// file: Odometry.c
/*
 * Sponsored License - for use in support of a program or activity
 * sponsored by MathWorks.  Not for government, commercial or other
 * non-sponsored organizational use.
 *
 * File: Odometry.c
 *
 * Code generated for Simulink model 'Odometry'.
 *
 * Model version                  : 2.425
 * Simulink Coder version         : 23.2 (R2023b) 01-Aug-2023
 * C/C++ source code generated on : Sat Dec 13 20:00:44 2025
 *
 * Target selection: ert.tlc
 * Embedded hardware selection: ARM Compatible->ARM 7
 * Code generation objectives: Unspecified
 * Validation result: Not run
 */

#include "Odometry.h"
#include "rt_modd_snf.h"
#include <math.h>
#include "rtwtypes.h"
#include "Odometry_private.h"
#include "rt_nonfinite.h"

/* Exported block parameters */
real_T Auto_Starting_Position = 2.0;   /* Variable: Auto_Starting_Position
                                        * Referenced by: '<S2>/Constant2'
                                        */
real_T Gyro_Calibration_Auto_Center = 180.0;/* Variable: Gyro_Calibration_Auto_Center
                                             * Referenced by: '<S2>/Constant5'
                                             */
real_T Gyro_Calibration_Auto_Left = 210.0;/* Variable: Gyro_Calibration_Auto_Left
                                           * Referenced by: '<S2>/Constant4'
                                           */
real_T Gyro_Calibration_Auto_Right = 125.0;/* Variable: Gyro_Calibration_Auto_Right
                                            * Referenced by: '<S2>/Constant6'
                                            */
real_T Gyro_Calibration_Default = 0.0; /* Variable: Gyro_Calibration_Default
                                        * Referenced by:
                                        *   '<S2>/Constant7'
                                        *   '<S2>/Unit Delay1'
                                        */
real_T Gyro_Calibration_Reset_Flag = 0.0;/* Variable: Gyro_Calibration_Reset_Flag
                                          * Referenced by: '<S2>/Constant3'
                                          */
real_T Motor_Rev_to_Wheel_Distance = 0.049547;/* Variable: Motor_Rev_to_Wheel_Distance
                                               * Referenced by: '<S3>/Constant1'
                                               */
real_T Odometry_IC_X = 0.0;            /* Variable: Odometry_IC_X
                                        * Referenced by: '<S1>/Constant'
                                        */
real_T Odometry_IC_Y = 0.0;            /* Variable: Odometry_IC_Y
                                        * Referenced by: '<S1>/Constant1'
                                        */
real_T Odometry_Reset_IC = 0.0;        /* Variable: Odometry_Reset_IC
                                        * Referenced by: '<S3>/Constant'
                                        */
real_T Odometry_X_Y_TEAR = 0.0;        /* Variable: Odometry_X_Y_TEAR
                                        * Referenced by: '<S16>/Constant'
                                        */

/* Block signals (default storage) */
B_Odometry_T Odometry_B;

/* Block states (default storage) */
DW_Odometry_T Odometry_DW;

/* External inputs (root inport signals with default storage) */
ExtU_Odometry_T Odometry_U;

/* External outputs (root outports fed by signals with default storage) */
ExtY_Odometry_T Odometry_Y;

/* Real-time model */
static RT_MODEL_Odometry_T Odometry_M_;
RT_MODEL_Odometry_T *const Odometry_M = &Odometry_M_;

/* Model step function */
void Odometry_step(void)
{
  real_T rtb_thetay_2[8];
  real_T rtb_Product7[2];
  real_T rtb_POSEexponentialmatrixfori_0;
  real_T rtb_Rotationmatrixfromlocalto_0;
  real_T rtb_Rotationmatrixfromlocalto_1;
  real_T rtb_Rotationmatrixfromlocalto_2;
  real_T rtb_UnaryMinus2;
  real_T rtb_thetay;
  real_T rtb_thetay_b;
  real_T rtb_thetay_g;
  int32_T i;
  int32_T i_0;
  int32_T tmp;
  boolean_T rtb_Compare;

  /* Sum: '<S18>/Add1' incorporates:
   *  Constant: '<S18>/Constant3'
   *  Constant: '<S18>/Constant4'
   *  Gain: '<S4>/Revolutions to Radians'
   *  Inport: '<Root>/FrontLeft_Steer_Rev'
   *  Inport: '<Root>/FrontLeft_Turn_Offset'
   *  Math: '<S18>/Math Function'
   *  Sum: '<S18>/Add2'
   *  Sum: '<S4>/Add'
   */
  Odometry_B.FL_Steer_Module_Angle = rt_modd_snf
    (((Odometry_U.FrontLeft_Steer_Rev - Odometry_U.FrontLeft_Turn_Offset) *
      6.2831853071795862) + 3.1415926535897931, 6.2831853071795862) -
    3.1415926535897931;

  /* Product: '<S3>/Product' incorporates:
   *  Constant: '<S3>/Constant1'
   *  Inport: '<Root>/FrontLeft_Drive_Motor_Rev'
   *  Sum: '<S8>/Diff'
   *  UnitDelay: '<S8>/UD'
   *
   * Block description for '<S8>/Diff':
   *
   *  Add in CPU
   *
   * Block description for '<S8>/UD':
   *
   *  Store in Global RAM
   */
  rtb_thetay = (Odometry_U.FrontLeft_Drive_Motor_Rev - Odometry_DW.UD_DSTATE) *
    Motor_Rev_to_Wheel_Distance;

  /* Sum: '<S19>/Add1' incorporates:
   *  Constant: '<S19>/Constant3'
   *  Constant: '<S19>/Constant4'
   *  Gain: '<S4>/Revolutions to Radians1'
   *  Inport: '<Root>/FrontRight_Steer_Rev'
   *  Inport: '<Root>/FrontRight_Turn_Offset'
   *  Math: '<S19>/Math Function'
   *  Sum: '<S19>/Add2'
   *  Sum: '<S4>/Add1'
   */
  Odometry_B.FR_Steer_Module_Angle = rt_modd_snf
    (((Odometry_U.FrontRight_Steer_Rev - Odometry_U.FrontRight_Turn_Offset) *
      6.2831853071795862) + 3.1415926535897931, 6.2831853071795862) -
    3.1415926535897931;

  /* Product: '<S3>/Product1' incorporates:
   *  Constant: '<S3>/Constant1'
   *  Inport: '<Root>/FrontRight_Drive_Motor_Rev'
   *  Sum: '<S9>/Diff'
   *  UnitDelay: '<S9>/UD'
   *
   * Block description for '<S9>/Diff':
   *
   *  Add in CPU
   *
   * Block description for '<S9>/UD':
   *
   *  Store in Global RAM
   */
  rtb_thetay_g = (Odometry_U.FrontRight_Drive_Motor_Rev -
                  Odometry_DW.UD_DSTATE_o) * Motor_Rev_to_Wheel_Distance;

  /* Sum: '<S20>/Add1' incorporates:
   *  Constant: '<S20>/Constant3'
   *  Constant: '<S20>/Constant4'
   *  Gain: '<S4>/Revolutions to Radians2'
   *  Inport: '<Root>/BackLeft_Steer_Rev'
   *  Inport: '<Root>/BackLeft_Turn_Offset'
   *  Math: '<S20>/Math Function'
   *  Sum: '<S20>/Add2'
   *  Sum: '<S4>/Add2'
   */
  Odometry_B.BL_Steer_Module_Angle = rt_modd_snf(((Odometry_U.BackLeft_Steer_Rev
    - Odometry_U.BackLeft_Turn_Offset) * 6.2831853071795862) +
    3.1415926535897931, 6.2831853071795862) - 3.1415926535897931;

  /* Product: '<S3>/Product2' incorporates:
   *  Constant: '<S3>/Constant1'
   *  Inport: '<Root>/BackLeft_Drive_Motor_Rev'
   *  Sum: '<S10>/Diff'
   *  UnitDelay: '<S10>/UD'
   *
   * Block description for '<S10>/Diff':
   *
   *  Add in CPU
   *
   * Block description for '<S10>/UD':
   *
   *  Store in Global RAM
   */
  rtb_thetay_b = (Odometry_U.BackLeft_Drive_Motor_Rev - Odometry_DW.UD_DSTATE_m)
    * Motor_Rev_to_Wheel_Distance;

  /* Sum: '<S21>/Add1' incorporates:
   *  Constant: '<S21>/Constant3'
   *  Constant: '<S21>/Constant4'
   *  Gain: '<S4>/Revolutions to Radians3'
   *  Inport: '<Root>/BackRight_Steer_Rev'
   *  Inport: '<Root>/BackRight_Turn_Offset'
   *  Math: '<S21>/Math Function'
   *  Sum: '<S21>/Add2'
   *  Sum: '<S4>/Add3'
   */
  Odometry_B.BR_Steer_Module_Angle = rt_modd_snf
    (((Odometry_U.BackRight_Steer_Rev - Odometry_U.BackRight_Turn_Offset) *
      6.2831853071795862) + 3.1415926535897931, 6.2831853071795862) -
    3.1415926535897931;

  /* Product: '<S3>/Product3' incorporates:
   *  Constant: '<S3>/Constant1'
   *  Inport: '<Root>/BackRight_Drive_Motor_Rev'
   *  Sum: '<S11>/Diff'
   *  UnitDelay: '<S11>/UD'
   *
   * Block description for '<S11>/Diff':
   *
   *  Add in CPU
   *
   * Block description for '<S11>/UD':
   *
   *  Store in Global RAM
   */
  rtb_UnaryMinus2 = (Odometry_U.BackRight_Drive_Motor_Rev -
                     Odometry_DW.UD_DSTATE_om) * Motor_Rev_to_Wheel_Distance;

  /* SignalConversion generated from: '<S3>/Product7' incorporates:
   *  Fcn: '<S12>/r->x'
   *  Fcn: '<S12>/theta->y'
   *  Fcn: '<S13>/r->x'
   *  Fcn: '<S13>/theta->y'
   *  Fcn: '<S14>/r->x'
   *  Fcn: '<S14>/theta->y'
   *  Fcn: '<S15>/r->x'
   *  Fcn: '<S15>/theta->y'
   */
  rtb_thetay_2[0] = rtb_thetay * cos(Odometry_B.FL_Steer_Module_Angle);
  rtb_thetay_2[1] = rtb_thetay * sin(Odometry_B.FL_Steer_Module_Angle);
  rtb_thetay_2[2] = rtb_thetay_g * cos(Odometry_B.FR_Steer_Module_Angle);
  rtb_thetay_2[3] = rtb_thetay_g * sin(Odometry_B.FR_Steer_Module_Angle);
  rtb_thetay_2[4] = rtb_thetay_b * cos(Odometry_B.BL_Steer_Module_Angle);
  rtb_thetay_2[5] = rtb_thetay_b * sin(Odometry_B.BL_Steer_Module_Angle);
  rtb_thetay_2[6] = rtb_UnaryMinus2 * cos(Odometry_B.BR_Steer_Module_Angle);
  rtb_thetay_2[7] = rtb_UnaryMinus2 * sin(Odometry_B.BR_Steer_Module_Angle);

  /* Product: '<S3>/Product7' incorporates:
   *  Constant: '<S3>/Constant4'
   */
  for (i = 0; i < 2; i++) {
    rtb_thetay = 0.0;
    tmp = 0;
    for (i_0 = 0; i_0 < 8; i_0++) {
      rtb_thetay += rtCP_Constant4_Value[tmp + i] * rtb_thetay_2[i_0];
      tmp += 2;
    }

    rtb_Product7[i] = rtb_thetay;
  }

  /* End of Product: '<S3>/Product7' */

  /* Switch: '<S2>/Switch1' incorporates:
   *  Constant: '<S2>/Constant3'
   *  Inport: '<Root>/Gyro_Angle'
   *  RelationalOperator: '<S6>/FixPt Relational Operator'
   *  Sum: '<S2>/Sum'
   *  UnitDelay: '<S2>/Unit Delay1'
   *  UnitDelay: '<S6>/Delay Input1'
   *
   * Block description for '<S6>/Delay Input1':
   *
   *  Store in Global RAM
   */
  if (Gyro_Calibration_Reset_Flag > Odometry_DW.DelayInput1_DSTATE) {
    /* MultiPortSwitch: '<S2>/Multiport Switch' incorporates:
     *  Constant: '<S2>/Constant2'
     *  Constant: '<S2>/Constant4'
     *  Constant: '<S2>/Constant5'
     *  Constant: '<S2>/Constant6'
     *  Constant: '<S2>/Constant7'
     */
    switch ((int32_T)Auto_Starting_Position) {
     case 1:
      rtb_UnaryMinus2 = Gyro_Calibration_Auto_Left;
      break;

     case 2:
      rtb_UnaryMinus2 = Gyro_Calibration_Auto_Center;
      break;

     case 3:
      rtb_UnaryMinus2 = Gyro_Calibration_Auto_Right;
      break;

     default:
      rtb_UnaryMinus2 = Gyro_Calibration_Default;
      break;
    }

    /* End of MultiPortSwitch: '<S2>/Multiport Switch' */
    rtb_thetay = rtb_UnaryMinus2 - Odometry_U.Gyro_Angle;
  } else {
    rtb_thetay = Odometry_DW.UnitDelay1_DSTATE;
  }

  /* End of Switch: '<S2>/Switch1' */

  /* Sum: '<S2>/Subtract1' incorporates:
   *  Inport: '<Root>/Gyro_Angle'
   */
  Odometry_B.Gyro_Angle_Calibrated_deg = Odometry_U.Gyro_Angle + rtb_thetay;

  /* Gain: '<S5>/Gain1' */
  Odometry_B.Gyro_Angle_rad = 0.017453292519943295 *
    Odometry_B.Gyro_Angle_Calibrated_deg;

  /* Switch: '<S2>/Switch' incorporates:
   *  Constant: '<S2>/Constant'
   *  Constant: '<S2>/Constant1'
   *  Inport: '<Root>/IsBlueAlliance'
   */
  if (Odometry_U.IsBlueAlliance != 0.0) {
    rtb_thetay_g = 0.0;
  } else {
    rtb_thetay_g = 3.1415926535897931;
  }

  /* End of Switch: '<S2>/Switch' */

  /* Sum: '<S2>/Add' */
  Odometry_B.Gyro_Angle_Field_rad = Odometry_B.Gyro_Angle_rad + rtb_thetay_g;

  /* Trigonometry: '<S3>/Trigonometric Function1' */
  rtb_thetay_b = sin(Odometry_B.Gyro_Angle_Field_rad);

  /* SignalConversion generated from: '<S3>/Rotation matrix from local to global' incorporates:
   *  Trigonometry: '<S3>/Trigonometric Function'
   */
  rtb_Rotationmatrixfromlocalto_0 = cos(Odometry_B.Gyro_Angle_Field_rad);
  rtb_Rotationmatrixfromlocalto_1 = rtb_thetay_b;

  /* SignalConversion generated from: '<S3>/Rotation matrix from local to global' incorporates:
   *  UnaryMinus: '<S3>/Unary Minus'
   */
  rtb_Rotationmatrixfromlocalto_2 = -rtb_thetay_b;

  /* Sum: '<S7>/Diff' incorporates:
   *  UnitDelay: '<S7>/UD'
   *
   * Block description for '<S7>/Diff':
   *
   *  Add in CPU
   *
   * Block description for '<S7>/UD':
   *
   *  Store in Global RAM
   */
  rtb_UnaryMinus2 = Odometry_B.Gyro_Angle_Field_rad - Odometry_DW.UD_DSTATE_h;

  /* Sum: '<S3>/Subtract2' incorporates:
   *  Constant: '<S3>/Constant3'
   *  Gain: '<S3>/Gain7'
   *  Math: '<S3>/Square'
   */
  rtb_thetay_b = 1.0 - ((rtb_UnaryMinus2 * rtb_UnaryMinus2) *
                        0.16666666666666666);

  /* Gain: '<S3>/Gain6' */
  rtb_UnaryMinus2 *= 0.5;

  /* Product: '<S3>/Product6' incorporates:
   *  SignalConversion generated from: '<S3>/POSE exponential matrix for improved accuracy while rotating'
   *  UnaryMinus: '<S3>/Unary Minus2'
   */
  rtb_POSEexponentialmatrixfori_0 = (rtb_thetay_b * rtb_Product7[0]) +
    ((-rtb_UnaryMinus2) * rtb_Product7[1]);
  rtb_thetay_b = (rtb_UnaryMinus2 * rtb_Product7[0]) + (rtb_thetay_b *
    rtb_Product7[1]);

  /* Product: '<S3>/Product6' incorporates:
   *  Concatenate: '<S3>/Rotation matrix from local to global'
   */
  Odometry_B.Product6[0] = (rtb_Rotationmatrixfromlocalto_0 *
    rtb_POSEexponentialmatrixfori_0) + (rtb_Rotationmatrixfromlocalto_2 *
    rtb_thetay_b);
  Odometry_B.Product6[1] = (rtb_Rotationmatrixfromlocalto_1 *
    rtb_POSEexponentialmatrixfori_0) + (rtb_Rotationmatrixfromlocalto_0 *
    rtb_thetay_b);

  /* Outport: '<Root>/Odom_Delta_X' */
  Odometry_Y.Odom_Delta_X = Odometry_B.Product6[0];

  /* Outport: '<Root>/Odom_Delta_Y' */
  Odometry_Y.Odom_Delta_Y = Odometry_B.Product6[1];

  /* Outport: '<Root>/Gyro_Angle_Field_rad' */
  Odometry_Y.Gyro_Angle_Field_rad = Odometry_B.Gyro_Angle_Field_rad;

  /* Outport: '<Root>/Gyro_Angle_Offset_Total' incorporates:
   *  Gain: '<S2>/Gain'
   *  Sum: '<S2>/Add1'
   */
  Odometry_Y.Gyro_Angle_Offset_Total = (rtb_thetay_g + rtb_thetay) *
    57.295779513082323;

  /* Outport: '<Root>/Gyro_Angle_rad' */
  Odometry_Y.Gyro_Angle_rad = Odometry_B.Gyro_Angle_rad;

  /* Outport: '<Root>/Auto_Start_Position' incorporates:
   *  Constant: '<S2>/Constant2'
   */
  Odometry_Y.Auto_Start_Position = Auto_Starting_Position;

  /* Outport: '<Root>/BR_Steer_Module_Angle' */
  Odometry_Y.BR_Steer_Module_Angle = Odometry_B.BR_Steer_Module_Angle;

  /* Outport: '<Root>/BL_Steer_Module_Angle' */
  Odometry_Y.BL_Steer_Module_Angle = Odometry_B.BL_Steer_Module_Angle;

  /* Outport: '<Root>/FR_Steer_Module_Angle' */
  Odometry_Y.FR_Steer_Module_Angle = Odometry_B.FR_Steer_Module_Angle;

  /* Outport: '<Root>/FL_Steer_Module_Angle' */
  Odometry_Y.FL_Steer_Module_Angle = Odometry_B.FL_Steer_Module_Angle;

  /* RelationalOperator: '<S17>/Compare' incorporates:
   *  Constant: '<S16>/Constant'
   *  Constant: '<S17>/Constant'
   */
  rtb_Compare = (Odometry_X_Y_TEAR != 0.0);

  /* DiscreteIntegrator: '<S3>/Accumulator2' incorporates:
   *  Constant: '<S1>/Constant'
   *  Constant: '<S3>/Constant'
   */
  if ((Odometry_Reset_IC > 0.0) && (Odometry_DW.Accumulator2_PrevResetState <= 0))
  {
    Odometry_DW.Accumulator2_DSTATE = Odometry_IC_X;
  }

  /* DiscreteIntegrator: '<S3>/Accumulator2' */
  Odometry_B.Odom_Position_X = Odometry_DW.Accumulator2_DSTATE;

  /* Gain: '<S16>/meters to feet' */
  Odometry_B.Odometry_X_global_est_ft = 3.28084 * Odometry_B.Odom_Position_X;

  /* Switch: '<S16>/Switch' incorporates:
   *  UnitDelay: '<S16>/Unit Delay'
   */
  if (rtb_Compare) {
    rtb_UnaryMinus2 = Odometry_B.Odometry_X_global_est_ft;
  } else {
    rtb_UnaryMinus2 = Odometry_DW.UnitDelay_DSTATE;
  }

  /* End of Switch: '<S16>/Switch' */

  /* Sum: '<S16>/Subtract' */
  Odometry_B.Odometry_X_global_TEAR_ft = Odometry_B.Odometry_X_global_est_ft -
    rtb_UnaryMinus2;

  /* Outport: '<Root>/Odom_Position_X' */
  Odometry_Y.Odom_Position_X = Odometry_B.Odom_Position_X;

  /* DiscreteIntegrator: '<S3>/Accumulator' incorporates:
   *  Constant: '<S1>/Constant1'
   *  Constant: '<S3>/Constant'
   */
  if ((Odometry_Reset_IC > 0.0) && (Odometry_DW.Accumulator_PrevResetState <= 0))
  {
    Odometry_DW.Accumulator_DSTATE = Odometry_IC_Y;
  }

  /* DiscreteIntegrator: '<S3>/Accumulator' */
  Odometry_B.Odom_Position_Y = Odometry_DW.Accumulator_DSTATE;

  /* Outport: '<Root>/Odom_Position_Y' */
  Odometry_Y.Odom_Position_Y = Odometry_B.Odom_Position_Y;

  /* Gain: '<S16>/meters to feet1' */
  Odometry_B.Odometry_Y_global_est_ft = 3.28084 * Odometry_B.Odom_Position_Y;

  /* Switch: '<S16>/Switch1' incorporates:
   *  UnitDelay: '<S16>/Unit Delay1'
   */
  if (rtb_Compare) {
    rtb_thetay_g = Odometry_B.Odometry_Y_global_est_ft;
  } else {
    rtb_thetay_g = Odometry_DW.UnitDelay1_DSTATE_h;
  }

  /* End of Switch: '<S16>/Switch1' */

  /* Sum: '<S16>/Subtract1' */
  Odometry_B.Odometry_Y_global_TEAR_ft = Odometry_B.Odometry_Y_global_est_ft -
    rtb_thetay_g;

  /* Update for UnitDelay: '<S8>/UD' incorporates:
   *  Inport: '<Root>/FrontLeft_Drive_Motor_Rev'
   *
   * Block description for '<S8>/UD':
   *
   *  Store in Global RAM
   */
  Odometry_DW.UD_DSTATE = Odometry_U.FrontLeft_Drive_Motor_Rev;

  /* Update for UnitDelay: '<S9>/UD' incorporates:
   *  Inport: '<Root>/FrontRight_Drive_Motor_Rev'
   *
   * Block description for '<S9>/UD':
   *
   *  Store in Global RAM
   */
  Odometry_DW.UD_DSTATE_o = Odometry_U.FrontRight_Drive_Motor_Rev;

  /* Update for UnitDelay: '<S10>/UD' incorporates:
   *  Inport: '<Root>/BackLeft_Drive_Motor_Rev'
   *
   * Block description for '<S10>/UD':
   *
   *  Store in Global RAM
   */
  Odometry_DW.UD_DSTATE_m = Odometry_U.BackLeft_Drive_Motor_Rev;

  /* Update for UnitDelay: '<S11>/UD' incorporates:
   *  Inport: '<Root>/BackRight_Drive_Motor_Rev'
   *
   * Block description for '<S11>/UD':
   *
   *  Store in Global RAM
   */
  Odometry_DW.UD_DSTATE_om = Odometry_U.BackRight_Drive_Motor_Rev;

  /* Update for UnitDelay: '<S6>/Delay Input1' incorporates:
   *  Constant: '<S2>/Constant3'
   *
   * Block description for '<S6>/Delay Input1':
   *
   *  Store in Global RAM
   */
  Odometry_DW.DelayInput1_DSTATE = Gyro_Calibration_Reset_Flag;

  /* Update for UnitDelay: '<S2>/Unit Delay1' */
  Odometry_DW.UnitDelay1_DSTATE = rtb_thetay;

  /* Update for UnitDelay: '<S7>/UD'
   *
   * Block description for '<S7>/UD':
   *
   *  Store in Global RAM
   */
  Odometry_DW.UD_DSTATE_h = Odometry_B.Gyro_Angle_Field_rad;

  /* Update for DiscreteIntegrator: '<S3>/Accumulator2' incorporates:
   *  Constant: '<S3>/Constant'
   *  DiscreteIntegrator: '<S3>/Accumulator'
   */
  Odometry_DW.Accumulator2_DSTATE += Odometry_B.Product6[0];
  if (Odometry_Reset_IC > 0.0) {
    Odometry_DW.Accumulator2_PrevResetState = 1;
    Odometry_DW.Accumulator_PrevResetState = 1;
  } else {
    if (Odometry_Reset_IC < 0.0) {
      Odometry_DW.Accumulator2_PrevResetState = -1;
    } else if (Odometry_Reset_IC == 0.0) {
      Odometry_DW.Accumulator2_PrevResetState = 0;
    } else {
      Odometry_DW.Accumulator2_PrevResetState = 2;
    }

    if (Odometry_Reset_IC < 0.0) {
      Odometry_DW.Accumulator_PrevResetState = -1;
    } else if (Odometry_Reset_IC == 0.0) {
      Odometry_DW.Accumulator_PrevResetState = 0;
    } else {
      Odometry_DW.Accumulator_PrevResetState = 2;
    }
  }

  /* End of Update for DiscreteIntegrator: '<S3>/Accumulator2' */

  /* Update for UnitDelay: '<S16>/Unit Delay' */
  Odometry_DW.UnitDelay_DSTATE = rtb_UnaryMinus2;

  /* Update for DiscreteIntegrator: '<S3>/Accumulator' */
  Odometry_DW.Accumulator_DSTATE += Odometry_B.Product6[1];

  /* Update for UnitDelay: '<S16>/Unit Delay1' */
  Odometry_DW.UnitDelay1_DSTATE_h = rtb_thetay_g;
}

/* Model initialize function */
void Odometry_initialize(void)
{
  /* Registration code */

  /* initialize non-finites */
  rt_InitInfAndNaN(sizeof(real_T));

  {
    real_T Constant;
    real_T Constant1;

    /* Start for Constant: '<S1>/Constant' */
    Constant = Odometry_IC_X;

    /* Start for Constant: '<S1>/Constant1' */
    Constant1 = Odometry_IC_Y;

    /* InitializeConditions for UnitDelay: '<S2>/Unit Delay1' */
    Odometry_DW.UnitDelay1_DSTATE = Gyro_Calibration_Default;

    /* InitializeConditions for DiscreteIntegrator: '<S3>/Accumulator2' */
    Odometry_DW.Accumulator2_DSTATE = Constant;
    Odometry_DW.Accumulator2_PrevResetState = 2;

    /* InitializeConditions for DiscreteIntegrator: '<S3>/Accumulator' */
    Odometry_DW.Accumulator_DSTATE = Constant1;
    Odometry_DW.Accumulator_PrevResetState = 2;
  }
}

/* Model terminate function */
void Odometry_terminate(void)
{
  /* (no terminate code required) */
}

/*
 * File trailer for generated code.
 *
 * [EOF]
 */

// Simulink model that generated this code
simulink model "Odometry"  (R2023b)
settings: Solver=FixedStepDiscrete  StartTime=0.0  StopTime=inf  FixedStep=t_sample_fast  RelTol=1e-3
undefined symbols (not defined in the file): Odometry_IC_X, Odometry_IC_Y, t_sample_fast

== system Odometry ==
  IsBlueAlliance : Inport
  Gyro_Angle : Inport  Port=2
  FrontLeft_Drive_Motor_Rev : Inport  Port=3
  FrontRight_Drive_Motor_Rev : Inport  Port=4
  BackLeft_Drive_Motor_Rev : Inport  Port=5
  BackRight_Drive_Motor_Rev : Inport  Port=6
  FrontLeft_Steer_Rev : Inport  Port=7
  FrontRight_Steer_Rev : Inport  Port=8
  BackLeft_Steer_Rev : Inport  Port=9
  BackRight_Steer_Rev : Inport  Port=10
  FrontLeft_Turn_Offset : Inport  Port=11
  FrontRight_Turn_Offset : Inport  Port=12
  BackLeft_Turn_Offset : Inport  Port=13
  BackRight_Turn_Offset : Inport  Port=14
  Odometry : Subsystem  SystemSampleTime=t_sample_fast  RTWFcnName=High_Frequency_Model_Step
  Gyro_Angle_Field_rad : Outport
  Gyro_Angle_rad : Outport  Port=2
  Gyro_Angle_Offset_Total : Outport  Port=3
  Auto_Start_Position : Outport  Port=4
  FL_Steer_Module_Angle : Outport  Port=5  OutDataTypeStr=double  Unit=rad
  FR_Steer_Module_Angle : Outport  Port=6  OutDataTypeStr=double  Unit=rad
  BL_Steer_Module_Angle : Outport  Port=7  OutDataTypeStr=double  Unit=rad
  BR_Steer_Module_Angle : Outport  Port=8  OutDataTypeStr=double  Unit=rad
  Odom_Position_X : Outport  Port=9
  Odom_Position_Y : Outport  Port=10
  Odom_Delta_X : Outport  Port=11
  Odom_Delta_Y : Outport  Port=12
  wires:
  FrontLeft_Drive_Motor_Rev/1 -> Odometry/3(FrontLeft_Drive_Motor_Rev)
  FrontRight_Drive_Motor_Rev/1 -> Odometry/4(FrontRight_Drive_Motor_Rev)
  Gyro_Angle/1 -> Odometry/2(Gyro_Angle)
  BackLeft_Drive_Motor_Rev/1 -> Odometry/5(BackLeft_Drive_Motor_Rev)
  IsBlueAlliance/1 -> Odometry/1(IsBlueAlliance)
  BackRight_Drive_Motor_Rev/1 -> Odometry/6(BackRight_Drive_Motor_Rev)
  FrontLeft_Steer_Rev/1 -> Odometry/7(FrontLeft_Steer_Rev)
  FrontRight_Steer_Rev/1 -> Odometry/8(FrontRight_Steer_Rev)
  BackLeft_Steer_Rev/1 -> Odometry/9(BackLeft_Steer_Rev)
  BackRight_Steer_Rev/1 -> Odometry/10(BackRight_Steer_Rev)
  FrontLeft_Turn_Offset/1 -> Odometry/11(FrontLeft_Turn_Offset)
  FrontRight_Turn_Offset/1 -> Odometry/12(FrontRight_Turn_Offset)
  BackLeft_Turn_Offset/1 -> Odometry/13(BackLeft_Turn_Offset)
  BackRight_Turn_Offset/1 -> Odometry/14(BackRight_Turn_Offset)
  Odometry/1(Gyro_Angle_Field_rad) -> Gyro_Angle_Field_rad/1
  Odometry/2(Gyro_Angle_rad) -> Gyro_Angle_rad/1
  Odometry/3(Gyro_Angle_Offset_Total) -> Gyro_Angle_Offset_Total/1
  Odometry/5(FL_Steer_Module_Angle) -> FL_Steer_Module_Angle/1
  Odometry/6(FR_Steer_Module_Angle) -> FR_Steer_Module_Angle/1
  Odometry/7(BL_Steer_Module_Angle) -> BL_Steer_Module_Angle/1
  Odometry/8(BR_Steer_Module_Angle) -> BR_Steer_Module_Angle/1
  Odometry/9(Odom_Position_X) -> Odom_Position_X/1
  Odometry/10(Odom_Position_Y) -> Odom_Position_Y/1
  Odometry/11(Odom_Delta_X) -> Odom_Delta_X/1
  Odometry/12(Odom_Delta_Y) -> Odom_Delta_Y/1
  Odometry/4(Auto_Start_Position) -> Auto_Start_Position/1

== system Odometry/Odometry ==
  IsBlueAlliance : Inport
  Gyro_Angle : Inport  Port=2
  FrontLeft_Drive_Motor_Rev : Inport  Port=3
  FrontRight_Drive_Motor_Rev : Inport  Port=4
  BackLeft_Drive_Motor_Rev : Inport  Port=5
  BackRight_Drive_Motor_Rev : Inport  Port=6
  FrontLeft_Steer_Rev : Inport  Port=7
  FrontRight_Steer_Rev : Inport  Port=8
  BackLeft_Steer_Rev : Inport  Port=9
  BackRight_Steer_Rev : Inport  Port=10
  FrontLeft_Turn_Offset : Inport  Port=11
  FrontRight_Turn_Offset : Inport  Port=12
  BackLeft_Turn_Offset : Inport  Port=13
  BackRight_Turn_Offset : Inport  Port=14
  Bus Creator : BusCreator  Inputs=14
  Bus Selector : BusSelector  OutputSignals=FrontLeft_Steer_Rev,FrontLeft_Turn_Offset,FrontRight_Steer_Rev,FrontRight_Turn_Offset,BackLeft_Steer_Rev,BackLeft_Turn_Offset,BackRight_Steer_Rev,BackRight_Turn_Offset
  Bus Selector1 : BusSelector  OutputSignals=FrontLeft_Drive_Motor_Rev,FrontRight_Drive_Motor_Rev,BackLeft_Drive_Motor_Rev,BackRight_Drive_Motor_Rev
  Bus Selector2 : BusSelector  OutputSignals=Gyro_Angle,IsBlueAlliance
  Constant : Constant  Value=Odometry_IC_X
  Constant1 : Constant  Value=Odometry_IC_Y
  Gyro_Angles : Subsystem  ReferencedSubsystem=Gyro_Angles
  Odometry : Subsystem  ReferencedSubsystem=Odometry_sub
  Steer_Module_Offset_Adjustments : Subsystem  ReferencedSubsystem=Steer_Module_Offset_Adjustments_sub
  Gyro_Angle_Field_rad : Outport
  Gyro_Angle_rad : Outport  Port=2
  Gyro_Angle_Offset_Total : Outport  Port=3
  Auto_Start_Position : Outport  Port=4
  FL_Steer_Module_Angle : Outport  Port=5  OutDataTypeStr=double  Unit=rad
  FR_Steer_Module_Angle : Outport  Port=6  OutDataTypeStr=double  Unit=rad
  BL_Steer_Module_Angle : Outport  Port=7  OutDataTypeStr=double  Unit=rad
  BR_Steer_Module_Angle : Outport  Port=8  OutDataTypeStr=double  Unit=rad
  Odom_Position_X : Outport  Port=9
  Odom_Position_Y : Outport  Port=10
  Odom_Delta_X : Outport  Port=11
  Odom_Delta_Y : Outport  Port=12
  wires:
  Constant/1 -> Odometry/9
  Constant1/1 -> Odometry/10
  Gyro_Angles/1 -> Odometry/11, Gyro_Angle_Field_rad/1
  Steer_Module_Offset_Adjustments/1 -> FL_Steer_Module_Angle/1, Odometry/5
  Steer_Module_Offset_Adjustments/2 -> FR_Steer_Module_Angle/1, Odometry/6
  Steer_Module_Offset_Adjustments/3 -> BL_Steer_Module_Angle/1, Odometry/7
  Steer_Module_Offset_Adjustments/4 -> BR_Steer_Module_Angle/1, Odometry/8
  Odometry/1 -> Odom_Position_X/1
  Odometry/2 -> Odom_Position_Y/1
  Odometry/3 -> Odom_Delta_X/1
  Odometry/4 -> Odom_Delta_Y/1
  Gyro_Angles/2 -> Gyro_Angle_rad/1
  Gyro_Angles/3 -> Gyro_Angle_Offset_Total/1
  BackRight_Turn_Offset/1 -> Bus Creator/13  "BackRight_Turn_Offset"
  BackLeft_Turn_Offset/1 -> Bus Creator/12  "BackLeft_Turn_Offset"
  FrontRight_Turn_Offset/1 -> Bus Creator/11  "FrontRight_Turn_Offset"
  FrontLeft_Turn_Offset/1 -> Bus Creator/10  "FrontLeft_Turn_Offset"
  BackRight_Steer_Rev/1 -> Bus Creator/9  "BackRight_Steer_Rev"
  BackLeft_Steer_Rev/1 -> Bus Creator/8  "BackLeft_Steer_Rev"
  FrontRight_Steer_Rev/1 -> Bus Creator/7  "FrontRight_Steer_Rev"
  FrontLeft_Steer_Rev/1 -> Bus Creator/6  "FrontLeft_Steer_Rev"
  BackRight_Drive_Motor_Rev/1 -> Bus Creator/5  "BackRight_Drive_Motor_Rev"
  BackLeft_Drive_Motor_Rev/1 -> Bus Creator/4  "BackLeft_Drive_Motor_Rev"
  FrontRight_Drive_Motor_Rev/1 -> Bus Creator/3  "FrontRight_Drive_Motor_Rev"
  FrontLeft_Drive_Motor_Rev/1 -> Bus Creator/2  "FrontLeft_Drive_Motor_Rev"
  Gyro_Angle/1 -> Bus Creator/1  "Gyro_Angle"
  Bus Creator/1 -> Bus Selector1/1, Bus Selector2/1, Bus Selector/1
  Bus Selector/5 -> Steer_Module_Offset_Adjustments/5  "<BackLeft_Steer_Rev>"
  Bus Selector/4 -> Steer_Module_Offset_Adjustments/4  "<FrontRight_Turn_Offset>"
  Bus Selector/6 -> Steer_Module_Offset_Adjustments/6  "<BackLeft_Turn_Offset>"
  Bus Selector/3 -> Steer_Module_Offset_Adjustments/3  "<FrontRight_Steer_Rev>"
  Bus Selector/7 -> Steer_Module_Offset_Adjustments/7  "<BackRight_Steer_Rev>"
  Bus Selector/2 -> Steer_Module_Offset_Adjustments/2  "<FrontLeft_Turn_Offset>"
  Bus Selector/8 -> Steer_Module_Offset_Adjustments/8  "<BackRight_Turn_Offset>"
  Bus Selector/1 -> Steer_Module_Offset_Adjustments/1  "<FrontLeft_Steer_Rev>"
  Bus Selector1/1 -> Odometry/1  "<FrontLeft_Drive_Motor_Rev>"
  Bus Selector1/2 -> Odometry/2  "<FrontRight_Drive_Motor_Rev>"
  Bus Selector1/3 -> Odometry/3  "<BackLeft_Drive_Motor_Rev>"
  Bus Selector1/4 -> Odometry/4  "<BackRight_Drive_Motor_Rev>"
  Bus Selector2/1 -> Gyro_Angles/1  "<Gyro_Angle>"
  IsBlueAlliance/1 -> Bus Creator/14  "IsBlueAlliance"
  Bus Selector2/2 -> Gyro_Angles/2  "<IsBlueAlliance>"
  Gyro_Angles/4 -> Auto_Start_Position/1
